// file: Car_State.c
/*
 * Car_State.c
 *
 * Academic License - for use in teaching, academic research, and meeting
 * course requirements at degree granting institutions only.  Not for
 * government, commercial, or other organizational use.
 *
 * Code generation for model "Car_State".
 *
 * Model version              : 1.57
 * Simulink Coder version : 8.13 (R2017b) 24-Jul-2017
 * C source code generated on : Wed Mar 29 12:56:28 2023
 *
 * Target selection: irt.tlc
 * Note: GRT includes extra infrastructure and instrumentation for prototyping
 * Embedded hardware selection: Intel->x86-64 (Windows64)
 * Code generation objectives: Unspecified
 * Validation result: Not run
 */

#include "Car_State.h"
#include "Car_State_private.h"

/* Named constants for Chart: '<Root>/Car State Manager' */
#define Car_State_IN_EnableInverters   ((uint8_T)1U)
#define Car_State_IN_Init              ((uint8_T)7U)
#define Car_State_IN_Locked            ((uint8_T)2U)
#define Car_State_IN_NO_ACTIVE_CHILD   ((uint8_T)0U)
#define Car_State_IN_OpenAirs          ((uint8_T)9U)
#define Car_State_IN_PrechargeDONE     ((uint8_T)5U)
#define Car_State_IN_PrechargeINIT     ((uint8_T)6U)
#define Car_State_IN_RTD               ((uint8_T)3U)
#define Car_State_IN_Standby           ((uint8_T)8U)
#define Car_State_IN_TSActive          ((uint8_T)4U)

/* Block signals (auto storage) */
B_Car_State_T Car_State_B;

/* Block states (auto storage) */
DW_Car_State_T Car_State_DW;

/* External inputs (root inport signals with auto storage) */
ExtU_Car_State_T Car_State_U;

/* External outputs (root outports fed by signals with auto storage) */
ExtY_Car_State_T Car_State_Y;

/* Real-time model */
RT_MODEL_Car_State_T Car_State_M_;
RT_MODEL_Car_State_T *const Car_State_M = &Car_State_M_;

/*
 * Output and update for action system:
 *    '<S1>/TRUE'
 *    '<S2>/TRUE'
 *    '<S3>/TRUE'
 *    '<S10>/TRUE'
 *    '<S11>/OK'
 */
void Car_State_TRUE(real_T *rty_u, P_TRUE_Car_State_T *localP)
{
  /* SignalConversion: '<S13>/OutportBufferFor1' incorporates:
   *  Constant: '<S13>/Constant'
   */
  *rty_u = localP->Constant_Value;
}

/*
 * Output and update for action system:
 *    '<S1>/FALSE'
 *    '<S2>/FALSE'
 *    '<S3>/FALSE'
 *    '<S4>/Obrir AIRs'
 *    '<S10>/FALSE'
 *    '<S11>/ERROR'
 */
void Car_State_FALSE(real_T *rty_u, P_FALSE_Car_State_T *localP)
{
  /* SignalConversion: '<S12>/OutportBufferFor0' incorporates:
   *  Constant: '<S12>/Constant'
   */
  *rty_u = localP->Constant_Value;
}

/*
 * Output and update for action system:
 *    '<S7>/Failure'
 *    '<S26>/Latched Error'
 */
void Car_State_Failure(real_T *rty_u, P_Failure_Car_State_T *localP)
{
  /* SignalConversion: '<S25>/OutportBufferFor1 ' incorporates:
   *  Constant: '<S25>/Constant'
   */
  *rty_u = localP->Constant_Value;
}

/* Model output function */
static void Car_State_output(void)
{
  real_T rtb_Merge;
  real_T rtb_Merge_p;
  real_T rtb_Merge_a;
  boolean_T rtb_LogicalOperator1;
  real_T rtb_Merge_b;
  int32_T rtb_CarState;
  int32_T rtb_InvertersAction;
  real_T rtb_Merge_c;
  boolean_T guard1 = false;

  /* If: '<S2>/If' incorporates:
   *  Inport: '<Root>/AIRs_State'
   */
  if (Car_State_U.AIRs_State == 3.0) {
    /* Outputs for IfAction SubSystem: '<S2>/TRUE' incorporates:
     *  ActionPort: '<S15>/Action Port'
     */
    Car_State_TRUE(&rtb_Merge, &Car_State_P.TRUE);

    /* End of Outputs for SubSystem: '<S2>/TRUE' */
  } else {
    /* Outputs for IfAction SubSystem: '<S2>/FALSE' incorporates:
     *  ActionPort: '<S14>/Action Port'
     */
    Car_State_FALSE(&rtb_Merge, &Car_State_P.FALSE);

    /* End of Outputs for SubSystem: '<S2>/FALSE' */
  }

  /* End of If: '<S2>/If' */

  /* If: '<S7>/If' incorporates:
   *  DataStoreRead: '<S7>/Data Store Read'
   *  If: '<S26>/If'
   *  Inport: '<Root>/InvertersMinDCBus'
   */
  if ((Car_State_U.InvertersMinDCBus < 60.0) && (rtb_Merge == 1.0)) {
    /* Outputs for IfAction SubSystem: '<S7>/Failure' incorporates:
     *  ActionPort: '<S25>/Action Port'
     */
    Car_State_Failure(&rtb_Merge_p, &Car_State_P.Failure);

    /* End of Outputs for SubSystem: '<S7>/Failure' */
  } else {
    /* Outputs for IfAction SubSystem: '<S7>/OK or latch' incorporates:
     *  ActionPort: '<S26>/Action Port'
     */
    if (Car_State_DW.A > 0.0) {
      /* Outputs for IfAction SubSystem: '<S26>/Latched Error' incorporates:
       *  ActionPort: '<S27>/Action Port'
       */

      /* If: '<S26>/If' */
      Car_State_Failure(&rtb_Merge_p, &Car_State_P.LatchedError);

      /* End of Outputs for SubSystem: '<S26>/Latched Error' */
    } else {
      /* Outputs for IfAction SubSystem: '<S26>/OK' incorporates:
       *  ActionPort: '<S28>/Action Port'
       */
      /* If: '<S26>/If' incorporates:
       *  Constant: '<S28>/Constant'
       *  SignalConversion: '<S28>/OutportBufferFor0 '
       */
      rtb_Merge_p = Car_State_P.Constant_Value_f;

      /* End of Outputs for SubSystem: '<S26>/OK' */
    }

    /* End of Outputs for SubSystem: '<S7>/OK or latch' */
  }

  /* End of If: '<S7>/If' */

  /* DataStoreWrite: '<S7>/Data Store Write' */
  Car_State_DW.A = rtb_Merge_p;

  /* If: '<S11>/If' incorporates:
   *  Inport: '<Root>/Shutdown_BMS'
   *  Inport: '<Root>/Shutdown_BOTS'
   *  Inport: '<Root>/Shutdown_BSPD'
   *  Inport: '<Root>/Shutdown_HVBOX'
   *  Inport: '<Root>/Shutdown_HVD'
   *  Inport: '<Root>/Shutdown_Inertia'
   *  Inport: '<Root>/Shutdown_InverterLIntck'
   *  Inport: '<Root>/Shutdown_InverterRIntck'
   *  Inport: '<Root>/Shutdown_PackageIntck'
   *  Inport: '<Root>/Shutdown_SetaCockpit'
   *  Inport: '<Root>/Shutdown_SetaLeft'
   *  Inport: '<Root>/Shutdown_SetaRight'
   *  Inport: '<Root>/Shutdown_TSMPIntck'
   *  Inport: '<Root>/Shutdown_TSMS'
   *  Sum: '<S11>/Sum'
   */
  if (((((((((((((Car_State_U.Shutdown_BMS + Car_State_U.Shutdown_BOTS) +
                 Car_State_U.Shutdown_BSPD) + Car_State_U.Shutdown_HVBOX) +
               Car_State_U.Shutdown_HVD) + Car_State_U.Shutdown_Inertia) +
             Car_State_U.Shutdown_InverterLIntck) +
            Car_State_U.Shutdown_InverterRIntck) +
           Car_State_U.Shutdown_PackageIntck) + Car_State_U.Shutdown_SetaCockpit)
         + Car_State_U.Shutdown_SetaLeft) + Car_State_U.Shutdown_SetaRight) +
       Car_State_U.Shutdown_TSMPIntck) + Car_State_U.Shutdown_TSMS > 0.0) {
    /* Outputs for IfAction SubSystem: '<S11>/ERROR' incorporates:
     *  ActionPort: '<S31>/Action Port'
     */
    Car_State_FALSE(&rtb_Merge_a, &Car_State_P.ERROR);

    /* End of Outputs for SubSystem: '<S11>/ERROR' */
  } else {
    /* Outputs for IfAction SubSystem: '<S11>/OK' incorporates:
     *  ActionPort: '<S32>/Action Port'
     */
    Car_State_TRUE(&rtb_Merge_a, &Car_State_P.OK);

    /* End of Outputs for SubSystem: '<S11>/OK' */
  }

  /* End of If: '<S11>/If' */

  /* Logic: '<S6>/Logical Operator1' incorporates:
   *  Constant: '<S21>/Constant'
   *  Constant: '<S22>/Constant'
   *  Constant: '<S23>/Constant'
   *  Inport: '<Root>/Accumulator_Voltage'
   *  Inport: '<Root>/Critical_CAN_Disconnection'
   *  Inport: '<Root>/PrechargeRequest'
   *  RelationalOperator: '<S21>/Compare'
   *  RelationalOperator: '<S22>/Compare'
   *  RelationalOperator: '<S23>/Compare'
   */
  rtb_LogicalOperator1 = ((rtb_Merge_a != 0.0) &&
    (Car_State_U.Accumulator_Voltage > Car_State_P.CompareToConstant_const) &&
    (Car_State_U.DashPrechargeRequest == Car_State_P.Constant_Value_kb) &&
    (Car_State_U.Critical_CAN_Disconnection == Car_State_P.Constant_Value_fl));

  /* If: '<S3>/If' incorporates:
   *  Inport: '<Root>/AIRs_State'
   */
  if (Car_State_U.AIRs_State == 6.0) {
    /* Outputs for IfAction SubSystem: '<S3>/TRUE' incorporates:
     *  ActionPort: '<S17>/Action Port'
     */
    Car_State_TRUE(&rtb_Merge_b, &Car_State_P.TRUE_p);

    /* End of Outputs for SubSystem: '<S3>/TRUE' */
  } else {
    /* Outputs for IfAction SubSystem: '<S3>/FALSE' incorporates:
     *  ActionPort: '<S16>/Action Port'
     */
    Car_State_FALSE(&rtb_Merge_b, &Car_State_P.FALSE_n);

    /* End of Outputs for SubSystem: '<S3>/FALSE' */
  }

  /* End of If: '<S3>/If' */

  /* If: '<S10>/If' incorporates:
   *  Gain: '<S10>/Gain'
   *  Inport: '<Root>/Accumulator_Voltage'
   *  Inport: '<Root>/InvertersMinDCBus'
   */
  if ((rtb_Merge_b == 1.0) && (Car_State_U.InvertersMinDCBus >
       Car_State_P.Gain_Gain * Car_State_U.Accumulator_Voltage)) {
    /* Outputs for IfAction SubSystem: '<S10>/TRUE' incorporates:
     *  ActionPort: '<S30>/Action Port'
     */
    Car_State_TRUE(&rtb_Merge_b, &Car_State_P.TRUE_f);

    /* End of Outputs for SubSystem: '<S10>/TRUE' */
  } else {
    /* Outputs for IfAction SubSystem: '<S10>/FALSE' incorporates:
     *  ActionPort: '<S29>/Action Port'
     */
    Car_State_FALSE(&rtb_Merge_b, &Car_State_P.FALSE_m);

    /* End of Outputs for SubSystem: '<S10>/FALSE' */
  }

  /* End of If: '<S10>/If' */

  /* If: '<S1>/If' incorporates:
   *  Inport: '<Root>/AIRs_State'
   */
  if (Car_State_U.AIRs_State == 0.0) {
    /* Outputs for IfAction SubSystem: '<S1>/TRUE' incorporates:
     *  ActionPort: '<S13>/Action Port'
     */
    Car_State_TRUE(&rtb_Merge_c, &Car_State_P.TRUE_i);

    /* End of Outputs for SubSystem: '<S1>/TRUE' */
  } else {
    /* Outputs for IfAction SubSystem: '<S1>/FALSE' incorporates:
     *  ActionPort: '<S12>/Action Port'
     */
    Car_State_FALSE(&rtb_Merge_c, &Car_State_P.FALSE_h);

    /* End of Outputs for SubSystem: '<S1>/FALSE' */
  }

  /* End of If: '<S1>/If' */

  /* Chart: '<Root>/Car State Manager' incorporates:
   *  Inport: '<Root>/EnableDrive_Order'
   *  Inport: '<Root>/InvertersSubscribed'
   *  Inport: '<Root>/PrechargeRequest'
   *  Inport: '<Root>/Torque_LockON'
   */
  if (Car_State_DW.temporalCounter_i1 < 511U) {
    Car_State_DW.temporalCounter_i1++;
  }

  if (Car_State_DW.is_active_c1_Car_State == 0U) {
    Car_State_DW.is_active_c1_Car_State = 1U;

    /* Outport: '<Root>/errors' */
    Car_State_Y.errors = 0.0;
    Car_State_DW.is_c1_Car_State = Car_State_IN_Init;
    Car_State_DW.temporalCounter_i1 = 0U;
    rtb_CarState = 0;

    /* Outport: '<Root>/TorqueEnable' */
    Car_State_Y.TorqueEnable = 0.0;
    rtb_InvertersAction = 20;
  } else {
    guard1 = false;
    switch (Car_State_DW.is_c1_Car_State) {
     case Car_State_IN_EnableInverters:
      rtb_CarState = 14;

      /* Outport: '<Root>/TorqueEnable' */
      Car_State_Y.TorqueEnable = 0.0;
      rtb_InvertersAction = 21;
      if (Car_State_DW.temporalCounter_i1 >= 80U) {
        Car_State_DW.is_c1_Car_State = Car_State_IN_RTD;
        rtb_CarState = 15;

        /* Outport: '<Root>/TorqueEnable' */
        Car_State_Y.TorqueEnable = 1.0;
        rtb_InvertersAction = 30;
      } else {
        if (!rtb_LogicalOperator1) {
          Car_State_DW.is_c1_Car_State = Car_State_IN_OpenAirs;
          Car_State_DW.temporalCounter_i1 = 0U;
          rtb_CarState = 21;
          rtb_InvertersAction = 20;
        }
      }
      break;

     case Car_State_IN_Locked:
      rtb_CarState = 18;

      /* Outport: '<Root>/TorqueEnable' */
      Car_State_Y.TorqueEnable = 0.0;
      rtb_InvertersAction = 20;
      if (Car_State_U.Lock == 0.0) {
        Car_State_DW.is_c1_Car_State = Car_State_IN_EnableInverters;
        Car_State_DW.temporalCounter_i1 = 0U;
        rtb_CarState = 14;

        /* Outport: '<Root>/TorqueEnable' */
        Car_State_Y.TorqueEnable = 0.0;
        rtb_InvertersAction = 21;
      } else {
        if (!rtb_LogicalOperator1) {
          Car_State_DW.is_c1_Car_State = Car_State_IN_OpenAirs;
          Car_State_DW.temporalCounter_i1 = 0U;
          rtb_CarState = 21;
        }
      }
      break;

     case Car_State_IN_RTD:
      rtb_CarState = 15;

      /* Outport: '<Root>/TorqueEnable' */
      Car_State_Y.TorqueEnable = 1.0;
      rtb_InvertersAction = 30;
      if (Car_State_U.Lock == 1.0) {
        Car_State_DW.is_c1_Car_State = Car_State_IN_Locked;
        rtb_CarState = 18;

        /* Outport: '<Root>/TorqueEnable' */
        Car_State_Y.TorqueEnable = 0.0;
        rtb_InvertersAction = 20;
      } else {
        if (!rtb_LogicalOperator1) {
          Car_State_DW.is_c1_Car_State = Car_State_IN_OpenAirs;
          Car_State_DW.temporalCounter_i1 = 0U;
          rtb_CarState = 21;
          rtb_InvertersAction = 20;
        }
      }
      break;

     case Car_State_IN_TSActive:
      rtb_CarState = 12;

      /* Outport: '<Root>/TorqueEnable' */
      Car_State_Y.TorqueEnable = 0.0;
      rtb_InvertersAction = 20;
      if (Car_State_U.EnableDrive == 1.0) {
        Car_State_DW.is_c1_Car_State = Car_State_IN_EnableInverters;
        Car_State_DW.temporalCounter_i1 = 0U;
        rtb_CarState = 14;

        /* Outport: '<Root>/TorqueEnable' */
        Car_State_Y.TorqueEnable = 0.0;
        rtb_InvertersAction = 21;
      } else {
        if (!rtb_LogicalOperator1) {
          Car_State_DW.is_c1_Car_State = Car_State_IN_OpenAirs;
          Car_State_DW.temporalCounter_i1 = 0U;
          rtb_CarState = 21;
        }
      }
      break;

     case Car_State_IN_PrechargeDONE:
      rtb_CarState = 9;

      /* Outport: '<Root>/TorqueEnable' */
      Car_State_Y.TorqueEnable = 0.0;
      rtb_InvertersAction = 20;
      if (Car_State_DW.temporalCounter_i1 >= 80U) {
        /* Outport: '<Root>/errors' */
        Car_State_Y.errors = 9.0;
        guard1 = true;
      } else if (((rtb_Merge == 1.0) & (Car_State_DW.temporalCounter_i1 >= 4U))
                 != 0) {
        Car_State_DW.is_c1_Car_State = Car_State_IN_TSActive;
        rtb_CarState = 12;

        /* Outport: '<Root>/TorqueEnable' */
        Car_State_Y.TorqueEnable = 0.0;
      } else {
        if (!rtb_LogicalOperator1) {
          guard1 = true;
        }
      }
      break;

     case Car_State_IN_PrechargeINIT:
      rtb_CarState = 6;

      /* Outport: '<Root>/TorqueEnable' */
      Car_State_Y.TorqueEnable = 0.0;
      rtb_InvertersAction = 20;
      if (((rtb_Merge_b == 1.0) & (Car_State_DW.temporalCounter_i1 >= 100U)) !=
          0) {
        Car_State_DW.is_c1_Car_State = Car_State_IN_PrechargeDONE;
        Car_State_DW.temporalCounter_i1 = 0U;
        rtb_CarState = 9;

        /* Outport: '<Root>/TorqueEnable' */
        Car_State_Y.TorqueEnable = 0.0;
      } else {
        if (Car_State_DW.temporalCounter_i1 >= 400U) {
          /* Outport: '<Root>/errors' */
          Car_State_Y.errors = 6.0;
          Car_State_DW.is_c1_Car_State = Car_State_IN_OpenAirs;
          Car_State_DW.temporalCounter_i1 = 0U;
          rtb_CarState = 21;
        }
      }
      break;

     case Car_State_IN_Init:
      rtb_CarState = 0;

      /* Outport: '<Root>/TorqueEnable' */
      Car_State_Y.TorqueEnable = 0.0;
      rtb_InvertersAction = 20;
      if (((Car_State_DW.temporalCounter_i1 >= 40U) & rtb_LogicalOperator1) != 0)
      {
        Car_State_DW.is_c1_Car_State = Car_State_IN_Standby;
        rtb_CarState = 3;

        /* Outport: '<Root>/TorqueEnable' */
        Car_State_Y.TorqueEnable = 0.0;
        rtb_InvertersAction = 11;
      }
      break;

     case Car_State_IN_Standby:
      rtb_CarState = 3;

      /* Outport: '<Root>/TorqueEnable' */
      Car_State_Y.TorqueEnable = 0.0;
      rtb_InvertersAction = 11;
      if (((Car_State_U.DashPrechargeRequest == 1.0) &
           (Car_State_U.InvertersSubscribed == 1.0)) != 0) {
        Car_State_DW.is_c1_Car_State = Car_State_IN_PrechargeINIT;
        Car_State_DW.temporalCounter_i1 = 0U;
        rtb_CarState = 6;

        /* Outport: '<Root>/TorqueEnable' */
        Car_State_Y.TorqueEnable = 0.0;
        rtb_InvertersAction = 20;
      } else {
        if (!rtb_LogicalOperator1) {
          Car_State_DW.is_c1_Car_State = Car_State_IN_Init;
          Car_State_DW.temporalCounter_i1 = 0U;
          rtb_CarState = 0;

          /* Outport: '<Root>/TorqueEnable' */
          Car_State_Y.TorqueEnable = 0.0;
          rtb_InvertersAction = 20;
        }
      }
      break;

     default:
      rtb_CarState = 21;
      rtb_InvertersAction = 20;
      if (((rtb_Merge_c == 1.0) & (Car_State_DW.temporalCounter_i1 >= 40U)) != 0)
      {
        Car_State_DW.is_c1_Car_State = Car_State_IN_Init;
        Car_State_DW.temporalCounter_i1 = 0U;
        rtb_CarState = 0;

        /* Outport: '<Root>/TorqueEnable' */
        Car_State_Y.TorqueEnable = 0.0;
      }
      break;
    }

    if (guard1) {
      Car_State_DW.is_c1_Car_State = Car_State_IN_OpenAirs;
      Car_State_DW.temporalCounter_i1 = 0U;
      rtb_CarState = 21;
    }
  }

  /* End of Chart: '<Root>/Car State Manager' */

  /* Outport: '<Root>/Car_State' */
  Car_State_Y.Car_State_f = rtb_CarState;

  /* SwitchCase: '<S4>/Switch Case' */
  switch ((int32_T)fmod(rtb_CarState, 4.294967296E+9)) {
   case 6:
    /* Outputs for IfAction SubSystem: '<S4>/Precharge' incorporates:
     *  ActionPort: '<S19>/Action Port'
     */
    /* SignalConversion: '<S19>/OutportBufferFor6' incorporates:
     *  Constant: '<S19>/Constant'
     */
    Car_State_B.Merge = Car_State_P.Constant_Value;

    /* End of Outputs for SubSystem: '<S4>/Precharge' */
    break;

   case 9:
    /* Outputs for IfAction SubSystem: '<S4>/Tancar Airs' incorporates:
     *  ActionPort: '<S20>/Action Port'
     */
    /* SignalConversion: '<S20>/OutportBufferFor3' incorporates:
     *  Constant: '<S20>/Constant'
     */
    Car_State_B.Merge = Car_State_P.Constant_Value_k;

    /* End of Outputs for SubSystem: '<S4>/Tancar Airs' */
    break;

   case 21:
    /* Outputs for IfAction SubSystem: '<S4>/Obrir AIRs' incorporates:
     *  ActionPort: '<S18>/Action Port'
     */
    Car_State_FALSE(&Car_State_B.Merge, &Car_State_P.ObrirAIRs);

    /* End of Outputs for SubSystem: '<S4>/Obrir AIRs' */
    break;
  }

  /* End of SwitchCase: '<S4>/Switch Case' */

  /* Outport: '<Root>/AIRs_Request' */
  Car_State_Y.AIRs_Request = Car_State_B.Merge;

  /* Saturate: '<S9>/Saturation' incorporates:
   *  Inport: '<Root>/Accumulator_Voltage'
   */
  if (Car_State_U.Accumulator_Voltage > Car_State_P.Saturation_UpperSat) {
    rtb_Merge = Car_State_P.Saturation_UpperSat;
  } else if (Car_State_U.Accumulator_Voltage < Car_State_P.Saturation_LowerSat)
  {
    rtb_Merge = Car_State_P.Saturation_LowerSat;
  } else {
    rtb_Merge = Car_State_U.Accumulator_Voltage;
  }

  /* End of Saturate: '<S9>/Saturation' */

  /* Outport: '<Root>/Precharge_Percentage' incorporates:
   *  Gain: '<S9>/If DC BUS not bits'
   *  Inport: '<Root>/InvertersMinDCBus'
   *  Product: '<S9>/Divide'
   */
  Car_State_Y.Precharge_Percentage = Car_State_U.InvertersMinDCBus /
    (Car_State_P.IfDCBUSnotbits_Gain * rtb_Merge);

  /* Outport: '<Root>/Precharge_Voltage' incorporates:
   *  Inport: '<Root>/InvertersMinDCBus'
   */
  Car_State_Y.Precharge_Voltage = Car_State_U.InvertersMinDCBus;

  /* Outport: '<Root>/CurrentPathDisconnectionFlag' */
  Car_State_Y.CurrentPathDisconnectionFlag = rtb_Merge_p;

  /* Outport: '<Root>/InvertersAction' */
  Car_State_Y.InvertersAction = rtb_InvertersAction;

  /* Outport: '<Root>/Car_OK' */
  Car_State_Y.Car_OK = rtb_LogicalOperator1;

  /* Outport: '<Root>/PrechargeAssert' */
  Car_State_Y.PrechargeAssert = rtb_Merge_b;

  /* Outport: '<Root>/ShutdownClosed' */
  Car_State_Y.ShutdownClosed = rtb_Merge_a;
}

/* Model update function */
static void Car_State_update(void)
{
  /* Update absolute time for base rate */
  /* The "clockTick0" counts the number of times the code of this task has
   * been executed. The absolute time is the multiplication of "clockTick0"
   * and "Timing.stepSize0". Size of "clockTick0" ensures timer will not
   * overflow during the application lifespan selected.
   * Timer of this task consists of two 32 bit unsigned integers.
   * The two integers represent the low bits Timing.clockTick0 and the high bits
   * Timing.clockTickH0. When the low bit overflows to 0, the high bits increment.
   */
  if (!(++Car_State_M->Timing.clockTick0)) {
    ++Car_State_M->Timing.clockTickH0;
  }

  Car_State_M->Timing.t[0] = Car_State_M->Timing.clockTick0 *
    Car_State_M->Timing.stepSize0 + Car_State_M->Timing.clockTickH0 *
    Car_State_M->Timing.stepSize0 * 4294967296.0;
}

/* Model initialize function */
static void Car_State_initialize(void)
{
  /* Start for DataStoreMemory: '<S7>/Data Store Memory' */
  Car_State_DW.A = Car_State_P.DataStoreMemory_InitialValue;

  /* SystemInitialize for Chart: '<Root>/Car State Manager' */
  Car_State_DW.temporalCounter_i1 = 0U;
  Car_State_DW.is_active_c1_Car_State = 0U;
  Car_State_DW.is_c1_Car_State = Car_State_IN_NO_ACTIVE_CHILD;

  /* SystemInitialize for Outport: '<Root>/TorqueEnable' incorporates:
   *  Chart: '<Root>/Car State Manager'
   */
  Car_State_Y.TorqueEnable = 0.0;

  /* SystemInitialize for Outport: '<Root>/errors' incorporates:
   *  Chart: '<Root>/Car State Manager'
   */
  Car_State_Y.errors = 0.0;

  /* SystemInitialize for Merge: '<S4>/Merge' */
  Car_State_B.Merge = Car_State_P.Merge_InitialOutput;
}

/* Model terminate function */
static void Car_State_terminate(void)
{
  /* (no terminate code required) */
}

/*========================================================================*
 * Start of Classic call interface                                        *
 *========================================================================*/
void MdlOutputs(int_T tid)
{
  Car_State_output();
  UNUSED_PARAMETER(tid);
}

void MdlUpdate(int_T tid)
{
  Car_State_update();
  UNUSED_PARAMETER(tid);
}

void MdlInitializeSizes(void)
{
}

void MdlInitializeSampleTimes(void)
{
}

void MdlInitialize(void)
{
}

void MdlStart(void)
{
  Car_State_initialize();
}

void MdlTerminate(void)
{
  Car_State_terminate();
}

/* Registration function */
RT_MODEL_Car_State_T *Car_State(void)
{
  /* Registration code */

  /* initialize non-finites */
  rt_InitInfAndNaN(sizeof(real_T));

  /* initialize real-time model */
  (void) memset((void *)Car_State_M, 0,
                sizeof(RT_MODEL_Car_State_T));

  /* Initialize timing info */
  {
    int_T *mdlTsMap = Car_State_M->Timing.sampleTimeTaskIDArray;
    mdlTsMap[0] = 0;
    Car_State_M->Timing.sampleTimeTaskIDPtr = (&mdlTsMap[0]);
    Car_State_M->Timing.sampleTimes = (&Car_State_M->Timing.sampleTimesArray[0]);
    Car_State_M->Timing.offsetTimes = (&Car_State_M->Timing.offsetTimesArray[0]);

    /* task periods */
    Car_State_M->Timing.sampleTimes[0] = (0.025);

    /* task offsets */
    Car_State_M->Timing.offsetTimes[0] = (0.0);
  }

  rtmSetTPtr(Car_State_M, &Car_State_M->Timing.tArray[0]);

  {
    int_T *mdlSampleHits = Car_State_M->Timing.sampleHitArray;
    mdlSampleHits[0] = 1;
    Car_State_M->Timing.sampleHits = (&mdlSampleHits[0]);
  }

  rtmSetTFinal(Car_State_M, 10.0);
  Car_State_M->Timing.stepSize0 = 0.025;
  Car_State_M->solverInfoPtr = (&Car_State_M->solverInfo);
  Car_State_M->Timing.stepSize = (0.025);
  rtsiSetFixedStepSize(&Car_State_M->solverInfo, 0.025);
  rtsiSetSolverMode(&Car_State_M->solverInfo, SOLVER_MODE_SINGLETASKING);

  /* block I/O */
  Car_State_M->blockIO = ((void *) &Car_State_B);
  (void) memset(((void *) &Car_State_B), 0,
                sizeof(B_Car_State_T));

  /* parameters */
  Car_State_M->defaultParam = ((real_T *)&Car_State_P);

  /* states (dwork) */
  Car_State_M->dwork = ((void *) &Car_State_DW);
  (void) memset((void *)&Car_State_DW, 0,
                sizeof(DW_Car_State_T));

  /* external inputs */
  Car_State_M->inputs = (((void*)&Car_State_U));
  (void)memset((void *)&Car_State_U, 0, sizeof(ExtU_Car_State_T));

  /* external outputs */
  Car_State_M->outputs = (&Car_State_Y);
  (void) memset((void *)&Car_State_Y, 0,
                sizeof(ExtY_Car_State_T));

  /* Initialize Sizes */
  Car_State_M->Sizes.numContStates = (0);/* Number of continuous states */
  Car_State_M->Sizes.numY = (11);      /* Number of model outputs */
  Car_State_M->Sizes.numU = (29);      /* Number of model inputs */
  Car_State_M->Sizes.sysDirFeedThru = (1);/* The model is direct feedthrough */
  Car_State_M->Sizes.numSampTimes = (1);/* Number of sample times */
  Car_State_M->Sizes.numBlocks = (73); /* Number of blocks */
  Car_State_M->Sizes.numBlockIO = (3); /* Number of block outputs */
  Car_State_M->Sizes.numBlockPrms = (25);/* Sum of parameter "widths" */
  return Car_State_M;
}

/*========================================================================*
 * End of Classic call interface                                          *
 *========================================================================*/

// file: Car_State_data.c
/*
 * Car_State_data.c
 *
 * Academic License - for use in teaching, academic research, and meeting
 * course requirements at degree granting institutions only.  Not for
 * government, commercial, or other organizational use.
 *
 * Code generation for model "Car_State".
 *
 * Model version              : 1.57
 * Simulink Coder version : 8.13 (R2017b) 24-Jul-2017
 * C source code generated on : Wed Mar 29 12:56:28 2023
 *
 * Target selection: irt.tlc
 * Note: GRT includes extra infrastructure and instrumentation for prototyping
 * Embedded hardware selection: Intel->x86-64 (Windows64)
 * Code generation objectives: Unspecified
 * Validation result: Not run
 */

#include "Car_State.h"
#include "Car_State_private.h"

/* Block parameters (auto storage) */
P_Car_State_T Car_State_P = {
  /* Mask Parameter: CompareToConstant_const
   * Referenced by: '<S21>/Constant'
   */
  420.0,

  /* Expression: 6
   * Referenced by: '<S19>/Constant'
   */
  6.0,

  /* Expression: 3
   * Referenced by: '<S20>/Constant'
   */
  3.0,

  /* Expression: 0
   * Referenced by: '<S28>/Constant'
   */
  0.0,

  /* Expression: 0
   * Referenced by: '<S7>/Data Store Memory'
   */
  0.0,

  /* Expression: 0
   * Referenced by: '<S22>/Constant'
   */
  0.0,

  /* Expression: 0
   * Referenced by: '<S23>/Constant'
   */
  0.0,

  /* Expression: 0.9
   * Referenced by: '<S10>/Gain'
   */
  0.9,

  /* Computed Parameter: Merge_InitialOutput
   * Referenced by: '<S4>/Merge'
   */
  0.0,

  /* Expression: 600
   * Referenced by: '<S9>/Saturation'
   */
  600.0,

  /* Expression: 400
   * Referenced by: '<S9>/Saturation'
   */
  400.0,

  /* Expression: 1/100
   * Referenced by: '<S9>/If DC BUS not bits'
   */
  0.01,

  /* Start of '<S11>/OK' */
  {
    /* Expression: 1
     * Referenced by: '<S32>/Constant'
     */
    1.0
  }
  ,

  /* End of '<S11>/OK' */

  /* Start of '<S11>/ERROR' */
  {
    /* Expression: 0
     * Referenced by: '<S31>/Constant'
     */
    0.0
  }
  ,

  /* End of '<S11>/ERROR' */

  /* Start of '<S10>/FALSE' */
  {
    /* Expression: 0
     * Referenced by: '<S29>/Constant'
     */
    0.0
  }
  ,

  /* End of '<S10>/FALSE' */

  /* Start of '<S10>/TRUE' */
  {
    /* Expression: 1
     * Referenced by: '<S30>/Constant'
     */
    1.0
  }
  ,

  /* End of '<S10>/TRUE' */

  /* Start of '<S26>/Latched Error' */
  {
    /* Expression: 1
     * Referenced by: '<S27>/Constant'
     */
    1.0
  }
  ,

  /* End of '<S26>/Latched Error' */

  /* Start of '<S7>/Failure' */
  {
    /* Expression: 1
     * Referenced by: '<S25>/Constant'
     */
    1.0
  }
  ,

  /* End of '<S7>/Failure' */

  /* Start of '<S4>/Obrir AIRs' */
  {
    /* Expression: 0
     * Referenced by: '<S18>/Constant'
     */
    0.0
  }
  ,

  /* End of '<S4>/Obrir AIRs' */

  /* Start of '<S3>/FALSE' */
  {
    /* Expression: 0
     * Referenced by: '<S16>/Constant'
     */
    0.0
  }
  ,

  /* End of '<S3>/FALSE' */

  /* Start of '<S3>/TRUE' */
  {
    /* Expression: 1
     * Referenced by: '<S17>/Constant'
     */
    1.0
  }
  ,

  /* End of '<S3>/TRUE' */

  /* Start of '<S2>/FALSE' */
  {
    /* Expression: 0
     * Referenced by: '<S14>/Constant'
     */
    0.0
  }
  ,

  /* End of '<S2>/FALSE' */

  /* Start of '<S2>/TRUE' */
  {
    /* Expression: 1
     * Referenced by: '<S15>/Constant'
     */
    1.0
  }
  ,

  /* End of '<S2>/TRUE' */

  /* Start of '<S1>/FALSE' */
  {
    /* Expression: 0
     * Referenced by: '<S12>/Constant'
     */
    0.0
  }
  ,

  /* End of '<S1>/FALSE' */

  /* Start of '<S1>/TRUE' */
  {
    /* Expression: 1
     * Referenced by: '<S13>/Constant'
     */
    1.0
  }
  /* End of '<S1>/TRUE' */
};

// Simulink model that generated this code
simulink model "Car_State"  (R2017b)
settings: Solver=FixedStepAuto  StartTime=0.0  StopTime=10.0  RelTol=1e-3
libraries: simulink x4

== system Car_State ==
  Shutdown_SetaRight : Inport
  Shutdown_SetaLeft : Inport  Port=2
  Shutdown_Inertia : Inport  Port=3
  Shutdown_BOTS : Inport  Port=4
  Shutdown_SetaCockpit : Inport  Port=5
  Shutdown_BMS : Inport  Port=6
  Shutdown_BSPD : Inport  Port=7
  Shutdown_HVBOX : Inport  Port=8
  Shutdown_HVD : Inport  Port=9
  Shutdown_InverterLIntck : Inport  Port=10
  Shutdown_InverterRIntck : Inport  Port=11
  Shutdown_TSMPIntck : Inport  Port=12
  Shutdown_PackageIntck : Inport  Port=13
  Shutdown_TSMS : Inport  Port=14
  AIRs_State : Inport  Port=15
  Accumulator_Voltage : Inport  Port=16
  PrechargeRequest : Inport  Port=17
  EnableDrive_Order : Inport  Port=18
  Torque_LockON : Inport  Port=19
  Critical_CAN_Disconnection : Inport  Port=20
  InvertersSubscribed : Inport  Port=21
  InvertersMinDCBus : Inport  Port=22
  BMSerror_UnderTemperature : Inport  Port=23
  BMSerror_OverTemperature : Inport  Port=24
  BMSerror_OverVoltage : Inport  Port=25
  BMSerror_UnderVoltage : Inport  Port=26
  BMSerror_CurrentSensDisc : Inport  Port=27
  BMSerror_NTCDisconnection : Inport  Port=28
  BMSerror_CANDisconnection : Inport  Port=29
  AIRSOpened : Subsystem
  AIRS_Closed : Subsystem
  AIRS_Precharge : Subsystem
  AIRS_Request : Subsystem
  BMSerror_VoltageDisconnection : InportShadow  Port=28
  Car State Manager : Stateflow chart  TreatAsAtomicUnit=on  SystemSampleTime=0.025
  CarOK Checks : Subsystem
  CurrentPathDisconnection Detection : Subsystem
  Fail & State Report : Subsystem
  Precharge Info : Subsystem
  PrechargeAssert Conditions : Subsystem
  Terminator : Terminator
  any element opened : Subsystem
  Car_State : Outport
  TorqueEnable : Outport  Port=2
  AIRs_Request : Outport  Port=3
  errors : Outport  Port=4
  Precharge_Percentage : Outport  Port=5
  Precharge_Voltage : Outport  Port=6
  CurrentPathDisconnectionFlag : Outport  Port=7
  InvertersAction : Outport  Port=8
  Car_OK : Outport  Port=9
  PrechargeAssert : Outport  Port=10
  ShutdownClosed : Outport  Port=11
  wires:
  Shutdown_TSMPIntck/1 -> any element opened/13(In14)
  Shutdown_SetaLeft/1 -> any element opened/11(In12)
  Shutdown_SetaRight/1 -> any element opened/12(In13)
  Shutdown_TSMS/1 -> any element opened/14(In15)
  Shutdown_HVBOX/1 -> any element opened/4(In4)
  Shutdown_InverterRIntck/1 -> any element opened/8(In9)
  Shutdown_HVD/1 -> any element opened/5(In5)
  Shutdown_Inertia/1 -> any element opened/6(In7)
  Shutdown_PackageIntck/1 -> any element opened/9(In10)
  Shutdown_InverterLIntck/1 -> any element opened/7(In8)
  Shutdown_SetaCockpit/1 -> any element opened/10(In11)
  Shutdown_BMS/1 -> any element opened/1(In1)
  Shutdown_BOTS/1 -> any element opened/2(In2)
  CurrentPathDisconnection Detection/1(PowerPathDisconnection) -> CurrentPathDisconnectionFlag/1
  Car State Manager/1(CarState) -> Car_State/1, AIRS_Request/1(CarState)
  InvertersMinDCBus/1 -> PrechargeAssert Conditions/1(VminInverter), Precharge Info/1(Min DC BUS in V), CurrentPathDisconnection Detection/1(Min DC BUS in V)
  [PrechargeRequest] -> CarOK Checks/1(DashPrechargeRequest)
  [Vaccumulator] -> CarOK Checks/4(Vaccumulator)
  Precharge Info/1(Precharge_Percent) -> Precharge_Percentage/1
  Accumulator_Voltage/1 -> PrechargeAssert Conditions/2(Vaccumulator), [Vaccumulator], Precharge Info/2(TOTAL_V_BMS)
  AIRS_Closed/1(AIRSClosed) -> Car State Manager/5(AIRSClosedAssert), CurrentPathDisconnection Detection/2(AIRS_Closed)  "AIRSClosedAssert"
  EnableDrive_Order/1 -> Car State Manager/6(EnableDrive)  "EnableDrive"
  Precharge Info/2(Precharge_Voltage) -> Precharge_Voltage/1
  AIRS_Request/1(AIRS_Request) -> AIRs_Request/1
  Car State Manager/4(InvertersAction) -> InvertersAction/1
  InvertersSubscribed/1 -> Car State Manager/3(InvertersSubscribed)
  Car State Manager/2(TorqueEnable) -> TorqueEnable/1
  Car State Manager/3(error) -> errors/1
  CarOK Checks/1(CarOK) -> Car_OK/1, Car State Manager/1(CarOK)
  AIRS_Precharge/1(AIRS_Precharge) -> PrechargeAssert Conditions/3(AIRS_Precharge)
  PrechargeRequest/1 -> [PrechargeRequest], Car State Manager/2(PrechargeRequest)  "DashPrechargeRequest"
  Torque_LockON/1 -> Car State Manager/7(Lock)  "Lock"
  AIRSOpened/1(AIRSOpened) -> Car State Manager/8(AIRSOpenedAssert)
  AIRs_State/1 -> AIRSOpened/1(AIRS_State), AIRS_Precharge/1(AIRS_State), AIRS_Closed/1(AIRS_State)
  PrechargeAssert Conditions/1(PrechargeAssert) -> PrechargeAssert/1, Car State Manager/4(PrechargeAssert)  "PrechargeAssert"
  Critical_CAN_Disconnection/1 -> CarOK Checks/3(CriticalCANDisconnection)
  any element opened/1(ShutdownClosed) -> ShutdownClosed/1, CarOK Checks/2(ShutdownClosed)
  Shutdown_BSPD/1 -> any element opened/3(In3)
  BMSerror_OverVoltage/1 -> Fail & State Report/3(BMSerror_OverVoltage)
  BMSerror_CurrentSensDisc/1 -> Fail & State Report/5(BMSerror_CurrentSensDisc)
  BMSerror_UnderVoltage/1 -> Fail & State Report/4(BMSerror_UnderVoltage)
  BMSerror_CANDisconnection/1 -> Fail & State Report/8(BMSerror_CANDisconnection)
  BMSerror_VoltageDisconnection/1 -> Fail & State Report/7(BMSerror_VoltageDisconnection)
  BMSerror_UnderTemperature/1 -> Fail & State Report/1(BMSerror_UnderTemperature)
  BMSerror_OverTemperature/1 -> Fail & State Report/2(BMSerror_OverTemperature)
  BMSerror_NTCDisconnection/1 -> Fail & State Report/6(BMSerror_NTCDisconnection)
  Fail & State Report/1(State&FailReport) -> Terminator/1

== system Car_State/AIRSOpened ==
  AIRS_State : Inport
  FALSE : Subsystem  TreatAsAtomicUnit=on
  If : If  IfExpression=u1==0
  Merge : Merge
  TRUE : Subsystem  TreatAsAtomicUnit=on
  AIRSOpened : Outport
  wires:
  Merge/1 -> AIRSOpened/1
  FALSE/1(0) -> Merge/2
  If/2 -> FALSE/Action
  TRUE/1(1) -> Merge/1
  If/1 -> TRUE/Action
  AIRS_State/1 -> If/1

== system Car_State/AIRS_Closed ==
  AIRS_State : Inport
  FALSE : Subsystem  TreatAsAtomicUnit=on
  If : If  IfExpression=u1==3
  Merge : Merge
  TRUE : Subsystem  TreatAsAtomicUnit=on
  AIRSClosed : Outport
  wires:
  Merge/1 -> AIRSClosed/1
  FALSE/1(0) -> Merge/2
  If/2 -> FALSE/Action
  TRUE/1(1) -> Merge/1
  If/1 -> TRUE/Action
  AIRS_State/1 -> If/1

== system Car_State/AIRS_Precharge ==
  AIRS_State : Inport
  FALSE : Subsystem  TreatAsAtomicUnit=on
  If : If  IfExpression=u1==6
  Merge : Merge
  TRUE : Subsystem  TreatAsAtomicUnit=on
  AIRS_Precharge : Outport
  wires:
  Merge/1 -> AIRS_Precharge/1
  FALSE/1(0) -> Merge/2
  If/2 -> FALSE/Action
  TRUE/1(1) -> Merge/1
  If/1 -> TRUE/Action
  AIRS_State/1 -> If/1

== system Car_State/AIRS_Request ==
  note: StandBy
  CarState : Inport
  Merge : Merge  Inputs=3
  Obrir AIRs : Subsystem  TreatAsAtomicUnit=on
  Precharge : Subsystem  TreatAsAtomicUnit=on
  Switch Case : SwitchCase  CaseConditions={6,9,21}
  Tancar Airs : Subsystem  TreatAsAtomicUnit=on
  Terminator : Terminator
  AIRS_Request : Outport
  wires:
  Merge/1 -> AIRS_Request/1
  Switch Case/2 -> Tancar Airs/Action  "PrechargeDONE"
  Switch Case/1 -> Precharge/Action  "PrechargeINIT"
  CarState/1 -> Switch Case/1
  Switch Case/3 -> Obrir AIRs/Action  "OpenAirs"
  Precharge/1(6) -> Merge/1
  Tancar Airs/1(3) -> Merge/2
  Obrir AIRs/1(0) -> Merge/3
  Switch Case/4 -> Terminator/1

== system Car_State/CarOK Checks ==
  DashPrechargeRequest : Inport
  ShutdownClosed : Inport  Port=2
  CriticalCANDisconnection : Inport  Port=3
  Vaccumulator : Inport  Port=4
  Compare To Constant : simulink/Logic and Bit Operations/Compare To Constant  relop=>  const=420  OutDataTypeStr=boolean
  Compare To Zero1 : simulink/Logic and Bit Operations/Compare To Zero  relop===  OutDataTypeStr=boolean
  Compare To Zero2 : simulink/Logic and Bit Operations/Compare To Zero  relop===  OutDataTypeStr=boolean
  Logical Operator1 : Logic  Inputs=4  AllPortsSameDT=off  OutDataTypeStr=boolean
  CarOK : Outport
  wires:
  ShutdownClosed/1 -> Logical Operator1/1
  Compare To Constant/1 -> Logical Operator1/2
  Logical Operator1/1 -> CarOK/1
  Vaccumulator/1 -> Compare To Constant/1
  DashPrechargeRequest/1 -> Compare To Zero1/1
  Compare To Zero1/1 -> Logical Operator1/3
  CriticalCANDisconnection/1 -> Compare To Zero2/1
  Compare To Zero2/1 -> Logical Operator1/4

== system Car_State/CurrentPathDisconnection Detection ==
  note: Abans aquesta comprovació es feia amb RTD.
      | Té molt més sentit ferho amb l'estat dels AIRS
  Min DC BUS in V : Inport
  AIRS_Closed : Inport  Port=2
  Data Store Memory : DataStoreMemory  ReadBeforeWriteMsg=warning  WriteAfterWriteMsg=warning  WriteAfterReadMsg=warning  ShowAdditionalParam=off
  Data Store Read : DataStoreRead
  Data Store Write : DataStoreWrite
  DocBlock : simulink/Model-Wide Utilities/DocBlock  DocumentType=Text
      content=|
      | This module checks if the power path is disconnected somehow.
      |
      | Examples of why this could happen:
      | - HVD Removed
      | - Blown Fuse
      | - Disconnected Cable
      | ...
  Failure : Subsystem  TreatAsAtomicUnit=on
  If : If  NumInputs=2  IfExpression=(u1<60)&(u2==1)
  Merge : Merge
  OK or latch : Subsystem  TreatAsAtomicUnit=on
  PowerPathDisconnection : Outport
  wires:
  OK or latch/1("Out ") -> Merge/2
  Merge/1 -> PowerPathDisconnection/1, Data Store Write/1
  If/2 -> OK or latch/Action
  Data Store Read/1 -> OK or latch/1(IN)
  If/1 -> Failure/Action
  Failure/1("1 ") -> Merge/1
  AIRS_Closed/1 -> If/2
  Min DC BUS in V/1 -> If/1

== system Car_State/Fail & State Report ==
  BMSerror_UnderTemperature : Inport
  BMSerror_OverTemperature : Inport  Port=2
  BMSerror_OverVoltage : Inport  Port=3
  BMSerror_UnderVoltage : Inport  Port=4
  BMSerror_CurrentSensDisc : Inport  Port=5
  BMSerror_NTCDisconnection : Inport  Port=6
  BMSerror_VoltageDisconnection : Inport  Port=7
  BMSerror_CANDisconnection : Inport  Port=8
  Add : Sum  Inputs=++++++++
  State&FailReport : Outport
  wires:
  BMSerror_OverTemperature/1 -> Add/2
  Add/1 -> State&FailReport/1
  BMSerror_UnderTemperature/1 -> Add/1
  BMSerror_OverVoltage/1 -> Add/3
  BMSerror_UnderVoltage/1 -> Add/4
  BMSerror_CurrentSensDisc/1 -> Add/5
  BMSerror_NTCDisconnection/1 -> Add/6
  BMSerror_VoltageDisconnection/1 -> Add/7
  BMSerror_CANDisconnection/1 -> Add/8

== system Car_State/Precharge Info ==
  Min DC BUS in V : Inport
  TOTAL_V_BMS : Inport  Port=2
  Divide : Product  Inputs=*/
  If DC BUS not bits : Gain  Gain=1/100
  Saturation : Saturate  UpperLimit=600  LowerLimit=400
  Precharge_Percent : Outport
  Precharge_Voltage : Outport  Port=2
  wires:
  Divide/1 -> Precharge_Percent/1
  Saturation/1 -> If DC BUS not bits/1
  Min DC BUS in V/1 -> Precharge_Voltage/1, Divide/1
  TOTAL_V_BMS/1 -> Saturation/1
  If DC BUS not bits/1 -> Divide/2

== system Car_State/PrechargeAssert Conditions ==
  VminInverter : Inport
  Vaccumulator : Inport  Port=2
  AIRS_Precharge : Inport  Port=3
  FALSE : Subsystem  TreatAsAtomicUnit=on
  Gain : Gain  Gain=0.9
  If : If  NumInputs=3  IfExpression=(u1==1)&(u2>u3)
  Merge : Merge
  TRUE : Subsystem  TreatAsAtomicUnit=on
  PrechargeAssert : Outport
  wires:
  Vaccumulator/1 -> Gain/1
  If/2 -> FALSE/Action
  Gain/1 -> If/3
  FALSE/1(0) -> Merge/2
  TRUE/1(1) -> Merge/1
  If/1 -> TRUE/Action
  Merge/1 -> PrechargeAssert/1
  VminInverter/1 -> If/2
  AIRS_Precharge/1 -> If/1

== system Car_State/any element opened ==
  note: 1 -> error
  In1 : Inport
  In2 : Inport  Port=2
  In3 : Inport  Port=3
  In4 : Inport  Port=4
  In5 : Inport  Port=5
  In7 : Inport  Port=6
  In8 : Inport  Port=7
  In9 : Inport  Port=8
  In10 : Inport  Port=9
  In11 : Inport  Port=10
  In12 : Inport  Port=11
  In13 : Inport  Port=12
  In14 : Inport  Port=13
  In15 : Inport  Port=14
  ERROR : Subsystem  TreatAsAtomicUnit=on
  If : If  IfExpression=u1>0
  Merge : Merge
  OK : Subsystem  TreatAsAtomicUnit=on
  Sum : Sum  Inputs=++++++++++++++
  ShutdownClosed : Outport
  wires:
  In7/1 -> Sum/6
  In9/1 -> Sum/8
  In8/1 -> Sum/7
  In4/1 -> Sum/4
  In2/1 -> Sum/2
  In11/1 -> Sum/10
  In5/1 -> Sum/5
  Sum/1 -> If/1
  In1/1 -> Sum/1
  In12/1 -> Sum/11
  In10/1 -> Sum/9
  Merge/1 -> ShutdownClosed/1
  In13/1 -> Sum/12
  OK/1(1) -> Merge/2
  ERROR/1(0) -> Merge/1
  If/2 -> OK/Action
  If/1 -> ERROR/Action
  In14/1 -> Sum/13
  In15/1 -> Sum/14
  In3/1 -> Sum/3

== system Car_State/AIRSOpened/FALSE ==
  Action Port : ActionPort  ActionType=else
  Constant : Constant  Value=0
  0 : Outport
  wires:
  Constant/1 -> 0/1

== system Car_State/AIRSOpened/TRUE ==
  Action Port : ActionPort  ActionType=then
  Constant : Constant
  1 : Outport
  wires:
  Constant/1 -> 1/1

== system Car_State/AIRS_Closed/FALSE ==
  Action Port : ActionPort  ActionType=else
  Constant : Constant  Value=0
  0 : Outport
  wires:
  Constant/1 -> 0/1

== system Car_State/AIRS_Closed/TRUE ==
  Action Port : ActionPort  ActionType=then
  Constant : Constant
  1 : Outport
  wires:
  Constant/1 -> 1/1

== system Car_State/AIRS_Precharge/FALSE ==
  Action Port : ActionPort  ActionType=else
  Constant : Constant  Value=0
  0 : Outport
  wires:
  Constant/1 -> 0/1

== system Car_State/AIRS_Precharge/TRUE ==
  Action Port : ActionPort  ActionType=then
  Constant : Constant
  1 : Outport
  wires:
  Constant/1 -> 1/1

== system Car_State/AIRS_Request/Obrir AIRs ==
  Action Port : ActionPort  ActionType=case
  Constant : Constant  Value=0
  0 : Outport
  wires:
  Constant/1 -> 0/1

== system Car_State/AIRS_Request/Precharge ==
  Action Port : ActionPort  ActionType=case
  Constant : Constant  Value=6
  6 : Outport
  wires:
  Constant/1 -> 6/1

== system Car_State/AIRS_Request/Tancar Airs ==
  Action Port : ActionPort  ActionType=case
  Constant : Constant  Value=3
  3 : Outport
  wires:
  Constant/1 -> 3/1

== system Car_State/CurrentPathDisconnection Detection/Failure ==
  Action Port : ActionPort  ActionType=then
  Constant : Constant
  "1 " : Outport
  wires:
  Constant/1 -> "1 "/1

== system Car_State/CurrentPathDisconnection Detection/OK or latch ==
  IN : Inport
  Action Port : ActionPort  ActionType=else
  If : If  IfExpression=(u1>0)
  Latched Error : Subsystem  TreatAsAtomicUnit=on
  Merge : Merge
  OK : Subsystem  TreatAsAtomicUnit=on
  "Out " : Outport
  wires:
  IN/1 -> If/1
  If/1 -> Latched Error/Action
  If/2 -> OK/Action
  Latched Error/1("1 ") -> Merge/1
  OK/1("0 ") -> Merge/2
  Merge/1 -> "Out "/1

== system Car_State/PrechargeAssert Conditions/FALSE ==
  Action Port : ActionPort  ActionType=else
  Constant : Constant  Value=0
  0 : Outport
  wires:
  Constant/1 -> 0/1

== system Car_State/PrechargeAssert Conditions/TRUE ==
  Action Port : ActionPort  ActionType=then
  Constant : Constant
  1 : Outport
  wires:
  Constant/1 -> 1/1

== system Car_State/any element opened/ERROR ==
  Action Port : ActionPort  ActionType=then
  Constant : Constant  Value=0
  0 : Outport
  wires:
  Constant/1 -> 0/1

== system Car_State/any element opened/OK ==
  Action Port : ActionPort  ActionType=else
  Constant : Constant
  1 : Outport
  wires:
  Constant/1 -> 1/1

== system Car_State/CurrentPathDisconnection Detection/OK or latch/Latched Error ==
  Action Port : ActionPort  ActionType=then
  Constant : Constant
  "1 " : Outport
  wires:
  Constant/1 -> "1 "/1

== system Car_State/CurrentPathDisconnection Detection/OK or latch/OK ==
  Action Port : ActionPort  ActionType=else
  Constant : Constant  Value=0
  "0 " : Outport
  wires:
  Constant/1 -> "0 "/1

== stateflow chart Car_State/Car State Manager ==
  state SAFESTATE [group]
    state Init
      entry: CarState=0;
      TorqueEnable=0;
      InvertersAction=20;
    state Standby
      entry: CarState=3;
      TorqueEnable=0;
      InvertersAction=11;
    (default) -> Init : {error=0}
    Standby -> Init [order 2] : [CarOK==0]
    Init -> Standby : [CarOK==1 & after(1, sec)]
  state STOP [group]
    state OpenAirs
      entry: CarState=21;
      InvertersAction=20;
  note: Inverter Actions that can be commanded to the inverters:
      |
      | Unsubscribe -> 10
      | Subscribe -> 11
      | DisableDrive -> 20
      | EnableDrive -> 21
      | TorqueCommand -> 30
  state PRECHARGE [group]
    state PrechargeINIT
      entry: CarState=6;
      TorqueEnable=0;
      InvertersAction=20;
    state PrechargeDONE
      entry: CarState=9;
      TorqueEnable=0;
      InvertersAction=20;
    PrechargeINIT -> PrechargeDONE [order 1] : [PrechargeAssert==1 & after(2500,msec)]
  state ACTIVE [group]
    state TSActive
      entry: CarState=12;
      TorqueEnable=0;
      InvertersAction=20;
    state EnableInverters
      entry: CarState=14;
      TorqueEnable=0;
      InvertersAction=21;
    state RTD
      entry: CarState=15;
      TorqueEnable=1;
      InvertersAction=30;
    state Locked
      entry: CarState=18;
      TorqueEnable=0;
      InvertersAction=20;
    RTD -> Locked [order 1] : [Lock==1]
    EnableInverters -> RTD [order 1] : [after(2,sec)]
    TSActive -> EnableInverters [order 1] : [EnableDrive==1]
    Locked -> EnableInverters [order 1] : [Lock==0]
  OpenAirs -> Init : [AIRSOpenedAssert==1 & after(1,sec)]
  Standby -> PrechargeINIT [order 1] : [PrechargeRequest==1 & InvertersSubscribed==1]
  PrechargeINIT -> OpenAirs [order 2] : after(10,sec)
      | {error=6}
  PrechargeDONE -> OpenAirs [order 3] : [CarOK==0]
  PrechargeDONE -> OpenAirs [order 1] : after(2,sec)
      | {error=9}
  TSActive -> OpenAirs [order 2] : [CarOK==0]
  EnableInverters -> OpenAirs [order 2] : [CarOK==0]
  RTD -> OpenAirs [order 2] : [CarOK==0]
  Locked -> OpenAirs [order 2] : [CarOK==0]
  PrechargeDONE -> TSActive [order 2] : [AIRSClosedAssert==1 & after(100,msec)]
  data: CarOK input; PrechargeRequest input; InvertersSubscribed input; CarState output double; PrechargeAssert input; AIRSClosedAssert input; EnableDrive input; Lock input double; AIRSOpenedAssert input; TorqueEnable output double; error output double; InvertersAction output double
